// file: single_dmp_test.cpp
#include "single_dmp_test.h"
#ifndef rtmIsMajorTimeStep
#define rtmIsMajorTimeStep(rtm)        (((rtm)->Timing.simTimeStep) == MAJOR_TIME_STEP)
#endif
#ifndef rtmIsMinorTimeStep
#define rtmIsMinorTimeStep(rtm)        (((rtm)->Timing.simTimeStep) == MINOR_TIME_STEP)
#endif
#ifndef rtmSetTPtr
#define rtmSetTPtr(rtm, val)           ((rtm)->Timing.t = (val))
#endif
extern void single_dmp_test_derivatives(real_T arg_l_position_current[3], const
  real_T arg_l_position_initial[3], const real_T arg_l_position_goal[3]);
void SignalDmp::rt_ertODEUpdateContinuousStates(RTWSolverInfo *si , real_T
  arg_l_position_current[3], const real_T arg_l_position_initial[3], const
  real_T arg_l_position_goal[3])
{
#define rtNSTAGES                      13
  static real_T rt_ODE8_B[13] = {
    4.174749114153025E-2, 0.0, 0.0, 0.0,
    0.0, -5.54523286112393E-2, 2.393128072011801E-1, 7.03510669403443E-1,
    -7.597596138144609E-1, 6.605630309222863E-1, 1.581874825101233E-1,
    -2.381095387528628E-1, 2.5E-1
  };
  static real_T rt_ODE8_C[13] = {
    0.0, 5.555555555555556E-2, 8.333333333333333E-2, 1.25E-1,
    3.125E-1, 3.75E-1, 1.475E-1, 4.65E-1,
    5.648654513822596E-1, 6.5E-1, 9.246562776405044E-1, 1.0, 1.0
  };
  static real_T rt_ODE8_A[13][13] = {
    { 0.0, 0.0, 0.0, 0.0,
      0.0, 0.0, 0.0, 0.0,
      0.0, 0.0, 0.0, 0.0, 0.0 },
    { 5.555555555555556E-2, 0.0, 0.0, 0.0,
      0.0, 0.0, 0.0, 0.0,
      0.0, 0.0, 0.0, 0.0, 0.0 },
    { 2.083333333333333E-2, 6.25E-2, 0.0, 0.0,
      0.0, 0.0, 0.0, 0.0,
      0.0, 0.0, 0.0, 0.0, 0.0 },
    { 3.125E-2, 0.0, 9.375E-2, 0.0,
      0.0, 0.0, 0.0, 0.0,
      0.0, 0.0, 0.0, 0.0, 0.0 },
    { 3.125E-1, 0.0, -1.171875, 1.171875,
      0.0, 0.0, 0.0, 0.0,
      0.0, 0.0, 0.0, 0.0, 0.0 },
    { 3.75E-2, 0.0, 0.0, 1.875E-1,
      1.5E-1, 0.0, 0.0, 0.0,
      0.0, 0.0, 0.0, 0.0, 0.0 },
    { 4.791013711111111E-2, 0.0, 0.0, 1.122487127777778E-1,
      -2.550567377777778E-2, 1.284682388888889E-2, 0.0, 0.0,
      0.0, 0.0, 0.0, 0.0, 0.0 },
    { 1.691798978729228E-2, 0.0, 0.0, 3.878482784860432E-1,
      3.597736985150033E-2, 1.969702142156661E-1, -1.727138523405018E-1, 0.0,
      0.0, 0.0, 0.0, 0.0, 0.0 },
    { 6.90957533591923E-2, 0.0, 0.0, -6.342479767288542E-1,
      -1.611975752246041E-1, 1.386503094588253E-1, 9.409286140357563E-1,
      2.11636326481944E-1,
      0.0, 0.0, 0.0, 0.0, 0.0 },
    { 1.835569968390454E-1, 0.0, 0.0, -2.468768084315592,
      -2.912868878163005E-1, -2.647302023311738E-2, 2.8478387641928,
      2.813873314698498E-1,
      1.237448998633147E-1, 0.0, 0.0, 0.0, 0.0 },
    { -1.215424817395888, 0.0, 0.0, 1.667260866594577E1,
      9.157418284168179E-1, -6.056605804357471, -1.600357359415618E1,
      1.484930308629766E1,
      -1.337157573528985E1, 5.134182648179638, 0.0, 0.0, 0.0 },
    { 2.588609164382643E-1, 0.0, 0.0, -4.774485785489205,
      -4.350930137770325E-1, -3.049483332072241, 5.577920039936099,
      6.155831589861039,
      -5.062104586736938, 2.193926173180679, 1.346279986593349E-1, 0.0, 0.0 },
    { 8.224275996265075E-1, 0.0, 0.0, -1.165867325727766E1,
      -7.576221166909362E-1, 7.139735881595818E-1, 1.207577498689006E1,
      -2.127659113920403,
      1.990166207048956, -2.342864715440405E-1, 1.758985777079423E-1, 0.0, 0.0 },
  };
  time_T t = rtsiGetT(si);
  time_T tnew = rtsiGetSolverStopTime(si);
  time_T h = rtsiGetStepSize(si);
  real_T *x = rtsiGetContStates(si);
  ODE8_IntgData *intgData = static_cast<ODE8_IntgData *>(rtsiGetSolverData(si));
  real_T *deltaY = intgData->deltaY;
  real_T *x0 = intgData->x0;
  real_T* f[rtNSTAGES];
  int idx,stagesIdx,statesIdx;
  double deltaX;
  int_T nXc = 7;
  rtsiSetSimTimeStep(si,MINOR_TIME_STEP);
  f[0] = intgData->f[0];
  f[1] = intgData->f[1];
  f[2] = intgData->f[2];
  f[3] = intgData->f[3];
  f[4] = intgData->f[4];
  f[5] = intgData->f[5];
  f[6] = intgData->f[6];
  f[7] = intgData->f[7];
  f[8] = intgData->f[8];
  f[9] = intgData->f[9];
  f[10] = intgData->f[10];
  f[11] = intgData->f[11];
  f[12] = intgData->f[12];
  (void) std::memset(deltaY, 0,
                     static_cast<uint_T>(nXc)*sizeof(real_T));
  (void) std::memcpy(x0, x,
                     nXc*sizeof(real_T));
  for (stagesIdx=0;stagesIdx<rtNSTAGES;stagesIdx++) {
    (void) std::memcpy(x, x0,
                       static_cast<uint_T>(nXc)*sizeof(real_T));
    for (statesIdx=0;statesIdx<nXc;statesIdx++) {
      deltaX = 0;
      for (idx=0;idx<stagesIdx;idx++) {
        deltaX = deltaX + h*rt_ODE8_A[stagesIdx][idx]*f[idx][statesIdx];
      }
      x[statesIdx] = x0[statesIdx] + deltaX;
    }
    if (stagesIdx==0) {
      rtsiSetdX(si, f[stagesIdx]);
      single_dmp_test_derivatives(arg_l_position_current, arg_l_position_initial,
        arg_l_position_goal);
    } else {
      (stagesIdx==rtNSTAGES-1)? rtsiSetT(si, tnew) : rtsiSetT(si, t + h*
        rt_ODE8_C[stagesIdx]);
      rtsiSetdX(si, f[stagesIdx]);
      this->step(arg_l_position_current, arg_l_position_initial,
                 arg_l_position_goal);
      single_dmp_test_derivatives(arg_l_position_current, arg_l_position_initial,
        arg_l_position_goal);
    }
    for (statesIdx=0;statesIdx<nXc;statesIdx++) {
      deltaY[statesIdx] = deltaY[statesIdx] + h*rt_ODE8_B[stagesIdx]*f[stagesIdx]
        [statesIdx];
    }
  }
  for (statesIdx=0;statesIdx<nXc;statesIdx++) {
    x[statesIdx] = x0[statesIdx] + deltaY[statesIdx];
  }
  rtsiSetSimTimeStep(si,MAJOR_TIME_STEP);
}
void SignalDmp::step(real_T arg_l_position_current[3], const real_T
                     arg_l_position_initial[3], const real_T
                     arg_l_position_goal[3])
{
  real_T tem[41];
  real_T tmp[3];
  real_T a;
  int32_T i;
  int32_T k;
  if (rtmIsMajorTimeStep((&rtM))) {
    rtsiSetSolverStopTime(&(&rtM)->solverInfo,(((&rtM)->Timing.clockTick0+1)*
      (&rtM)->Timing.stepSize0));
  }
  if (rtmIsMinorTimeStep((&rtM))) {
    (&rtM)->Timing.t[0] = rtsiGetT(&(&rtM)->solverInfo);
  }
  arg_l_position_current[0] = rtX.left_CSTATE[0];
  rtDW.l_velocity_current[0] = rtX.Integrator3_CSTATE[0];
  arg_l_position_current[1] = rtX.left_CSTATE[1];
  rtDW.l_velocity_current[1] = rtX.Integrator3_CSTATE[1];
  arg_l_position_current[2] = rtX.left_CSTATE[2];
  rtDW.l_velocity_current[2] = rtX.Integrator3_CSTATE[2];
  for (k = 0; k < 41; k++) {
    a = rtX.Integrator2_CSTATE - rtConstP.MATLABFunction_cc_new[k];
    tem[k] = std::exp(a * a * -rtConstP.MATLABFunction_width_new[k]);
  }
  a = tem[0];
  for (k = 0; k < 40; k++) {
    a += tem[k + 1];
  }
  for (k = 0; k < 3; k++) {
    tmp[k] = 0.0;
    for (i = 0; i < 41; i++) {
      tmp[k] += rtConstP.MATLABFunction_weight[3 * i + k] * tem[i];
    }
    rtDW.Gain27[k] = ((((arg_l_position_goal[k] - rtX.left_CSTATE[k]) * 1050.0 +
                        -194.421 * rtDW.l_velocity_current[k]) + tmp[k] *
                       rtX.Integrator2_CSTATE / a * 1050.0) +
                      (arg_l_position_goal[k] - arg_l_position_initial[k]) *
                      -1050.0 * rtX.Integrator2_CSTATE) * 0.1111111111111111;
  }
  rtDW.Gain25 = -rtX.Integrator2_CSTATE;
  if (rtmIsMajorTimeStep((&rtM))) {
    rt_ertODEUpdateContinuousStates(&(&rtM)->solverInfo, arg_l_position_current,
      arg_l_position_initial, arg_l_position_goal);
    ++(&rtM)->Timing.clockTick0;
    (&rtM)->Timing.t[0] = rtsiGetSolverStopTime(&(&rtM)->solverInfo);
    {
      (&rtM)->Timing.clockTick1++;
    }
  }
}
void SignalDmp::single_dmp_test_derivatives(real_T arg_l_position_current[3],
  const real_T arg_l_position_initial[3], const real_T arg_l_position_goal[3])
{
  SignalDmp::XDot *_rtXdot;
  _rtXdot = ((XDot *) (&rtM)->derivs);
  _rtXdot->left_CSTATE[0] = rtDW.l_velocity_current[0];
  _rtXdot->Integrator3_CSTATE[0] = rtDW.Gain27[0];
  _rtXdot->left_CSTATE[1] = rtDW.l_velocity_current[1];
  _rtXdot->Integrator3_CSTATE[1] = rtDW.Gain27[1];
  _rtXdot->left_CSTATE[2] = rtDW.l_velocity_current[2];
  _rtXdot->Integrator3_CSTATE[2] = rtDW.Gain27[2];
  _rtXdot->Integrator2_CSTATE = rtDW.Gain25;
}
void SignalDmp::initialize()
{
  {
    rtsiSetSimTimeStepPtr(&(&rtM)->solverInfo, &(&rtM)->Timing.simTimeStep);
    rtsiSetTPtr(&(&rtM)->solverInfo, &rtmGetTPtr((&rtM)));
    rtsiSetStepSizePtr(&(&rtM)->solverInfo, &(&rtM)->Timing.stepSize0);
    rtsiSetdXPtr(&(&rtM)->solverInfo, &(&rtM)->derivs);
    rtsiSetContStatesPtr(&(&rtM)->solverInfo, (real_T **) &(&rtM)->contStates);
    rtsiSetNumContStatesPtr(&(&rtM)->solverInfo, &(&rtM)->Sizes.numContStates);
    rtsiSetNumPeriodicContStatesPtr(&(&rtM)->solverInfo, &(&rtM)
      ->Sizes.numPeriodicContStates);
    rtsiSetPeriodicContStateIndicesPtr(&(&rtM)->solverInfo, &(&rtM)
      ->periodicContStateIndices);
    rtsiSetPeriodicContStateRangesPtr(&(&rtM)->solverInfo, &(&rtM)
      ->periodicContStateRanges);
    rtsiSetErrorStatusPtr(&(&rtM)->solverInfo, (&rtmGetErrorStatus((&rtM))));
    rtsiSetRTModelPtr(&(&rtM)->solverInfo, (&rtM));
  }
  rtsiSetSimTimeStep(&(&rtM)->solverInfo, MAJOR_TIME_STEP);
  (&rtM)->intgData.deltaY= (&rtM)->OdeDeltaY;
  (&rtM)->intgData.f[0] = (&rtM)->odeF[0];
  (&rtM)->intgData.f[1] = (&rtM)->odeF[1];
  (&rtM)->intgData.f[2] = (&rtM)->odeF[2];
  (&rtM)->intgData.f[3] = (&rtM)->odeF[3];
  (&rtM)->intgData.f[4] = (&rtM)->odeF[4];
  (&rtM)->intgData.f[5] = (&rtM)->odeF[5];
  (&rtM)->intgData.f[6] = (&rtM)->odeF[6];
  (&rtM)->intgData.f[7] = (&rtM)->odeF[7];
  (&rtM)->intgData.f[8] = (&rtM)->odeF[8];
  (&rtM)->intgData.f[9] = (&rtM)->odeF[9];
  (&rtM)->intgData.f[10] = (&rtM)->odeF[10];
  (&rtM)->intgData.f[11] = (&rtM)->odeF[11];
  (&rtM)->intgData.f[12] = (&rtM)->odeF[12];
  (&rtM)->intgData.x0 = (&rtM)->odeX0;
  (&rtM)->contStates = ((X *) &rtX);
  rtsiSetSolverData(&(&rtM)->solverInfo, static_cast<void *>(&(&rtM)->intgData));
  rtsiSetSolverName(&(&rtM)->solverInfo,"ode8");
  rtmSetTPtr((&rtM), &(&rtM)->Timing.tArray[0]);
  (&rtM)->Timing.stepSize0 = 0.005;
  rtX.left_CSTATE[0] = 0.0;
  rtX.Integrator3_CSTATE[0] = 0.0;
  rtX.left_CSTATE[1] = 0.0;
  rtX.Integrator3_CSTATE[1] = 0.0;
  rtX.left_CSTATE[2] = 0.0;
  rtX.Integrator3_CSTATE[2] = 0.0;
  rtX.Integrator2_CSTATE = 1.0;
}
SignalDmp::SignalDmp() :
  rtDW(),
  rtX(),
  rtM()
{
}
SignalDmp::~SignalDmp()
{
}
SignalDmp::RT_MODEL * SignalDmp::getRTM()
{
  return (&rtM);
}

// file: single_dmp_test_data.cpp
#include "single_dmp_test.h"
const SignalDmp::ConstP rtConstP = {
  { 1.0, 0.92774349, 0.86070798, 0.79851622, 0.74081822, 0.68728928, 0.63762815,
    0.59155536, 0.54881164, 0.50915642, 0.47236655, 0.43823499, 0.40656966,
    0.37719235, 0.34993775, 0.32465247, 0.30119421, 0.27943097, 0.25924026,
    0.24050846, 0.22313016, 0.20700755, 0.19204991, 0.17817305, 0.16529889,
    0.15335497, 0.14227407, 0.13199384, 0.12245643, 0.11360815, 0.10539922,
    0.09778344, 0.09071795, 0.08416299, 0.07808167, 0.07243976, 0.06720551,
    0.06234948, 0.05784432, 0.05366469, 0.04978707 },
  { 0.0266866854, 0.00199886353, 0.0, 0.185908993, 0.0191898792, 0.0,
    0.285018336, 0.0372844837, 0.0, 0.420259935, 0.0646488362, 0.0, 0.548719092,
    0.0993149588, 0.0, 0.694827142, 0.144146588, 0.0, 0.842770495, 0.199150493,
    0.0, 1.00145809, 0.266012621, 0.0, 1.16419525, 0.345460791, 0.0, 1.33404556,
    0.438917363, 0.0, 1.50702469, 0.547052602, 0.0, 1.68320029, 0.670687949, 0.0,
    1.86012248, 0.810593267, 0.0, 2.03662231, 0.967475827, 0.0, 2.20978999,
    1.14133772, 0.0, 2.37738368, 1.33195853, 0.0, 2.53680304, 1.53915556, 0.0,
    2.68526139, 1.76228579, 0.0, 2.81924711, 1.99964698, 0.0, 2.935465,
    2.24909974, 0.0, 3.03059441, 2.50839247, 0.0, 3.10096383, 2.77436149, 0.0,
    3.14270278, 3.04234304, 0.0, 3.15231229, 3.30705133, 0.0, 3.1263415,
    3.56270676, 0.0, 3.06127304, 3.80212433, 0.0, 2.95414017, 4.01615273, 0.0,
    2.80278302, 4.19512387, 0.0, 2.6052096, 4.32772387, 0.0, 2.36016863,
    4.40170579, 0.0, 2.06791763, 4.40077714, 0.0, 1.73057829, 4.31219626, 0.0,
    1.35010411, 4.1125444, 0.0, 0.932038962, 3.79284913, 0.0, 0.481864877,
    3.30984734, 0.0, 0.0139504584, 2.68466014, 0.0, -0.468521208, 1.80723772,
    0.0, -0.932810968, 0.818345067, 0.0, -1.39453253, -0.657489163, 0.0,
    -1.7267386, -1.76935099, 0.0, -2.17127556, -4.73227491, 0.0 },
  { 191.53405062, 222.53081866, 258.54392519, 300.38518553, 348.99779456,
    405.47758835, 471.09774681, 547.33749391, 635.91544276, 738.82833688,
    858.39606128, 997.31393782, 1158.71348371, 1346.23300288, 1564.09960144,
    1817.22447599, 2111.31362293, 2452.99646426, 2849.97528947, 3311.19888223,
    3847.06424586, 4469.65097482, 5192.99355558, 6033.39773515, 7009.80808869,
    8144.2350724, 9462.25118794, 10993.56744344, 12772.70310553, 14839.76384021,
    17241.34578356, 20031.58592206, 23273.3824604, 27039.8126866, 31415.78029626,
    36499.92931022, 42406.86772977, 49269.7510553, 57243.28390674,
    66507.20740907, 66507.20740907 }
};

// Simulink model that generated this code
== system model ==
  l_position_initial : Inport
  l_position_goal : Inport
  l_position_current : Outport  <- 1: left
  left : Integrator  InitialCondition=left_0  <- 1: Integrator3
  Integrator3 : Integrator  <- 1: Gain27
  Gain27 : Gain  Gain=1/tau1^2  <- 1: Sum#1
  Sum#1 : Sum  Inputs=++++  <- 1: Gain#1, 2: Gain#2, 3: Gain#3, 4: Product#1
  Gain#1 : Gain  Gain=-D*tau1  <- 1: Integrator3
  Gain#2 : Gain  Gain=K  <- 1: Sum#2
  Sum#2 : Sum  Inputs=-+  <- 1: left, 2: l_position_goal
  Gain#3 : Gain  Gain=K  <- 1: MATLABFunction
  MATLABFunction : MATLAB Function  <- 1: Integrator2
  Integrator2 : Integrator  InitialCondition=1  <- 1: Gain25
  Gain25 : Gain  Gain=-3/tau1  <- 1: Integrator2
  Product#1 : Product  <- 1: Gain#4, 2: Integrator2
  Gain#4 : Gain  Gain=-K  <- 1: Sum#3
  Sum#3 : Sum  Inputs=+-  <- 1: l_position_goal, 2: l_position_initial
== matlab function MATLABFunction ==
function out = fcn(u, width_new, weight, cc_new)

% if(u>2.5)
%     y=1;
% elseif(u>=0&&u<=2.5)
%     y=0;
% else
%         y=-1;
% end

tem=exp(-width_new.*(u-cc_new).^2)';
y=(weight * tem * u) / sum(tem) ;

out = y;
